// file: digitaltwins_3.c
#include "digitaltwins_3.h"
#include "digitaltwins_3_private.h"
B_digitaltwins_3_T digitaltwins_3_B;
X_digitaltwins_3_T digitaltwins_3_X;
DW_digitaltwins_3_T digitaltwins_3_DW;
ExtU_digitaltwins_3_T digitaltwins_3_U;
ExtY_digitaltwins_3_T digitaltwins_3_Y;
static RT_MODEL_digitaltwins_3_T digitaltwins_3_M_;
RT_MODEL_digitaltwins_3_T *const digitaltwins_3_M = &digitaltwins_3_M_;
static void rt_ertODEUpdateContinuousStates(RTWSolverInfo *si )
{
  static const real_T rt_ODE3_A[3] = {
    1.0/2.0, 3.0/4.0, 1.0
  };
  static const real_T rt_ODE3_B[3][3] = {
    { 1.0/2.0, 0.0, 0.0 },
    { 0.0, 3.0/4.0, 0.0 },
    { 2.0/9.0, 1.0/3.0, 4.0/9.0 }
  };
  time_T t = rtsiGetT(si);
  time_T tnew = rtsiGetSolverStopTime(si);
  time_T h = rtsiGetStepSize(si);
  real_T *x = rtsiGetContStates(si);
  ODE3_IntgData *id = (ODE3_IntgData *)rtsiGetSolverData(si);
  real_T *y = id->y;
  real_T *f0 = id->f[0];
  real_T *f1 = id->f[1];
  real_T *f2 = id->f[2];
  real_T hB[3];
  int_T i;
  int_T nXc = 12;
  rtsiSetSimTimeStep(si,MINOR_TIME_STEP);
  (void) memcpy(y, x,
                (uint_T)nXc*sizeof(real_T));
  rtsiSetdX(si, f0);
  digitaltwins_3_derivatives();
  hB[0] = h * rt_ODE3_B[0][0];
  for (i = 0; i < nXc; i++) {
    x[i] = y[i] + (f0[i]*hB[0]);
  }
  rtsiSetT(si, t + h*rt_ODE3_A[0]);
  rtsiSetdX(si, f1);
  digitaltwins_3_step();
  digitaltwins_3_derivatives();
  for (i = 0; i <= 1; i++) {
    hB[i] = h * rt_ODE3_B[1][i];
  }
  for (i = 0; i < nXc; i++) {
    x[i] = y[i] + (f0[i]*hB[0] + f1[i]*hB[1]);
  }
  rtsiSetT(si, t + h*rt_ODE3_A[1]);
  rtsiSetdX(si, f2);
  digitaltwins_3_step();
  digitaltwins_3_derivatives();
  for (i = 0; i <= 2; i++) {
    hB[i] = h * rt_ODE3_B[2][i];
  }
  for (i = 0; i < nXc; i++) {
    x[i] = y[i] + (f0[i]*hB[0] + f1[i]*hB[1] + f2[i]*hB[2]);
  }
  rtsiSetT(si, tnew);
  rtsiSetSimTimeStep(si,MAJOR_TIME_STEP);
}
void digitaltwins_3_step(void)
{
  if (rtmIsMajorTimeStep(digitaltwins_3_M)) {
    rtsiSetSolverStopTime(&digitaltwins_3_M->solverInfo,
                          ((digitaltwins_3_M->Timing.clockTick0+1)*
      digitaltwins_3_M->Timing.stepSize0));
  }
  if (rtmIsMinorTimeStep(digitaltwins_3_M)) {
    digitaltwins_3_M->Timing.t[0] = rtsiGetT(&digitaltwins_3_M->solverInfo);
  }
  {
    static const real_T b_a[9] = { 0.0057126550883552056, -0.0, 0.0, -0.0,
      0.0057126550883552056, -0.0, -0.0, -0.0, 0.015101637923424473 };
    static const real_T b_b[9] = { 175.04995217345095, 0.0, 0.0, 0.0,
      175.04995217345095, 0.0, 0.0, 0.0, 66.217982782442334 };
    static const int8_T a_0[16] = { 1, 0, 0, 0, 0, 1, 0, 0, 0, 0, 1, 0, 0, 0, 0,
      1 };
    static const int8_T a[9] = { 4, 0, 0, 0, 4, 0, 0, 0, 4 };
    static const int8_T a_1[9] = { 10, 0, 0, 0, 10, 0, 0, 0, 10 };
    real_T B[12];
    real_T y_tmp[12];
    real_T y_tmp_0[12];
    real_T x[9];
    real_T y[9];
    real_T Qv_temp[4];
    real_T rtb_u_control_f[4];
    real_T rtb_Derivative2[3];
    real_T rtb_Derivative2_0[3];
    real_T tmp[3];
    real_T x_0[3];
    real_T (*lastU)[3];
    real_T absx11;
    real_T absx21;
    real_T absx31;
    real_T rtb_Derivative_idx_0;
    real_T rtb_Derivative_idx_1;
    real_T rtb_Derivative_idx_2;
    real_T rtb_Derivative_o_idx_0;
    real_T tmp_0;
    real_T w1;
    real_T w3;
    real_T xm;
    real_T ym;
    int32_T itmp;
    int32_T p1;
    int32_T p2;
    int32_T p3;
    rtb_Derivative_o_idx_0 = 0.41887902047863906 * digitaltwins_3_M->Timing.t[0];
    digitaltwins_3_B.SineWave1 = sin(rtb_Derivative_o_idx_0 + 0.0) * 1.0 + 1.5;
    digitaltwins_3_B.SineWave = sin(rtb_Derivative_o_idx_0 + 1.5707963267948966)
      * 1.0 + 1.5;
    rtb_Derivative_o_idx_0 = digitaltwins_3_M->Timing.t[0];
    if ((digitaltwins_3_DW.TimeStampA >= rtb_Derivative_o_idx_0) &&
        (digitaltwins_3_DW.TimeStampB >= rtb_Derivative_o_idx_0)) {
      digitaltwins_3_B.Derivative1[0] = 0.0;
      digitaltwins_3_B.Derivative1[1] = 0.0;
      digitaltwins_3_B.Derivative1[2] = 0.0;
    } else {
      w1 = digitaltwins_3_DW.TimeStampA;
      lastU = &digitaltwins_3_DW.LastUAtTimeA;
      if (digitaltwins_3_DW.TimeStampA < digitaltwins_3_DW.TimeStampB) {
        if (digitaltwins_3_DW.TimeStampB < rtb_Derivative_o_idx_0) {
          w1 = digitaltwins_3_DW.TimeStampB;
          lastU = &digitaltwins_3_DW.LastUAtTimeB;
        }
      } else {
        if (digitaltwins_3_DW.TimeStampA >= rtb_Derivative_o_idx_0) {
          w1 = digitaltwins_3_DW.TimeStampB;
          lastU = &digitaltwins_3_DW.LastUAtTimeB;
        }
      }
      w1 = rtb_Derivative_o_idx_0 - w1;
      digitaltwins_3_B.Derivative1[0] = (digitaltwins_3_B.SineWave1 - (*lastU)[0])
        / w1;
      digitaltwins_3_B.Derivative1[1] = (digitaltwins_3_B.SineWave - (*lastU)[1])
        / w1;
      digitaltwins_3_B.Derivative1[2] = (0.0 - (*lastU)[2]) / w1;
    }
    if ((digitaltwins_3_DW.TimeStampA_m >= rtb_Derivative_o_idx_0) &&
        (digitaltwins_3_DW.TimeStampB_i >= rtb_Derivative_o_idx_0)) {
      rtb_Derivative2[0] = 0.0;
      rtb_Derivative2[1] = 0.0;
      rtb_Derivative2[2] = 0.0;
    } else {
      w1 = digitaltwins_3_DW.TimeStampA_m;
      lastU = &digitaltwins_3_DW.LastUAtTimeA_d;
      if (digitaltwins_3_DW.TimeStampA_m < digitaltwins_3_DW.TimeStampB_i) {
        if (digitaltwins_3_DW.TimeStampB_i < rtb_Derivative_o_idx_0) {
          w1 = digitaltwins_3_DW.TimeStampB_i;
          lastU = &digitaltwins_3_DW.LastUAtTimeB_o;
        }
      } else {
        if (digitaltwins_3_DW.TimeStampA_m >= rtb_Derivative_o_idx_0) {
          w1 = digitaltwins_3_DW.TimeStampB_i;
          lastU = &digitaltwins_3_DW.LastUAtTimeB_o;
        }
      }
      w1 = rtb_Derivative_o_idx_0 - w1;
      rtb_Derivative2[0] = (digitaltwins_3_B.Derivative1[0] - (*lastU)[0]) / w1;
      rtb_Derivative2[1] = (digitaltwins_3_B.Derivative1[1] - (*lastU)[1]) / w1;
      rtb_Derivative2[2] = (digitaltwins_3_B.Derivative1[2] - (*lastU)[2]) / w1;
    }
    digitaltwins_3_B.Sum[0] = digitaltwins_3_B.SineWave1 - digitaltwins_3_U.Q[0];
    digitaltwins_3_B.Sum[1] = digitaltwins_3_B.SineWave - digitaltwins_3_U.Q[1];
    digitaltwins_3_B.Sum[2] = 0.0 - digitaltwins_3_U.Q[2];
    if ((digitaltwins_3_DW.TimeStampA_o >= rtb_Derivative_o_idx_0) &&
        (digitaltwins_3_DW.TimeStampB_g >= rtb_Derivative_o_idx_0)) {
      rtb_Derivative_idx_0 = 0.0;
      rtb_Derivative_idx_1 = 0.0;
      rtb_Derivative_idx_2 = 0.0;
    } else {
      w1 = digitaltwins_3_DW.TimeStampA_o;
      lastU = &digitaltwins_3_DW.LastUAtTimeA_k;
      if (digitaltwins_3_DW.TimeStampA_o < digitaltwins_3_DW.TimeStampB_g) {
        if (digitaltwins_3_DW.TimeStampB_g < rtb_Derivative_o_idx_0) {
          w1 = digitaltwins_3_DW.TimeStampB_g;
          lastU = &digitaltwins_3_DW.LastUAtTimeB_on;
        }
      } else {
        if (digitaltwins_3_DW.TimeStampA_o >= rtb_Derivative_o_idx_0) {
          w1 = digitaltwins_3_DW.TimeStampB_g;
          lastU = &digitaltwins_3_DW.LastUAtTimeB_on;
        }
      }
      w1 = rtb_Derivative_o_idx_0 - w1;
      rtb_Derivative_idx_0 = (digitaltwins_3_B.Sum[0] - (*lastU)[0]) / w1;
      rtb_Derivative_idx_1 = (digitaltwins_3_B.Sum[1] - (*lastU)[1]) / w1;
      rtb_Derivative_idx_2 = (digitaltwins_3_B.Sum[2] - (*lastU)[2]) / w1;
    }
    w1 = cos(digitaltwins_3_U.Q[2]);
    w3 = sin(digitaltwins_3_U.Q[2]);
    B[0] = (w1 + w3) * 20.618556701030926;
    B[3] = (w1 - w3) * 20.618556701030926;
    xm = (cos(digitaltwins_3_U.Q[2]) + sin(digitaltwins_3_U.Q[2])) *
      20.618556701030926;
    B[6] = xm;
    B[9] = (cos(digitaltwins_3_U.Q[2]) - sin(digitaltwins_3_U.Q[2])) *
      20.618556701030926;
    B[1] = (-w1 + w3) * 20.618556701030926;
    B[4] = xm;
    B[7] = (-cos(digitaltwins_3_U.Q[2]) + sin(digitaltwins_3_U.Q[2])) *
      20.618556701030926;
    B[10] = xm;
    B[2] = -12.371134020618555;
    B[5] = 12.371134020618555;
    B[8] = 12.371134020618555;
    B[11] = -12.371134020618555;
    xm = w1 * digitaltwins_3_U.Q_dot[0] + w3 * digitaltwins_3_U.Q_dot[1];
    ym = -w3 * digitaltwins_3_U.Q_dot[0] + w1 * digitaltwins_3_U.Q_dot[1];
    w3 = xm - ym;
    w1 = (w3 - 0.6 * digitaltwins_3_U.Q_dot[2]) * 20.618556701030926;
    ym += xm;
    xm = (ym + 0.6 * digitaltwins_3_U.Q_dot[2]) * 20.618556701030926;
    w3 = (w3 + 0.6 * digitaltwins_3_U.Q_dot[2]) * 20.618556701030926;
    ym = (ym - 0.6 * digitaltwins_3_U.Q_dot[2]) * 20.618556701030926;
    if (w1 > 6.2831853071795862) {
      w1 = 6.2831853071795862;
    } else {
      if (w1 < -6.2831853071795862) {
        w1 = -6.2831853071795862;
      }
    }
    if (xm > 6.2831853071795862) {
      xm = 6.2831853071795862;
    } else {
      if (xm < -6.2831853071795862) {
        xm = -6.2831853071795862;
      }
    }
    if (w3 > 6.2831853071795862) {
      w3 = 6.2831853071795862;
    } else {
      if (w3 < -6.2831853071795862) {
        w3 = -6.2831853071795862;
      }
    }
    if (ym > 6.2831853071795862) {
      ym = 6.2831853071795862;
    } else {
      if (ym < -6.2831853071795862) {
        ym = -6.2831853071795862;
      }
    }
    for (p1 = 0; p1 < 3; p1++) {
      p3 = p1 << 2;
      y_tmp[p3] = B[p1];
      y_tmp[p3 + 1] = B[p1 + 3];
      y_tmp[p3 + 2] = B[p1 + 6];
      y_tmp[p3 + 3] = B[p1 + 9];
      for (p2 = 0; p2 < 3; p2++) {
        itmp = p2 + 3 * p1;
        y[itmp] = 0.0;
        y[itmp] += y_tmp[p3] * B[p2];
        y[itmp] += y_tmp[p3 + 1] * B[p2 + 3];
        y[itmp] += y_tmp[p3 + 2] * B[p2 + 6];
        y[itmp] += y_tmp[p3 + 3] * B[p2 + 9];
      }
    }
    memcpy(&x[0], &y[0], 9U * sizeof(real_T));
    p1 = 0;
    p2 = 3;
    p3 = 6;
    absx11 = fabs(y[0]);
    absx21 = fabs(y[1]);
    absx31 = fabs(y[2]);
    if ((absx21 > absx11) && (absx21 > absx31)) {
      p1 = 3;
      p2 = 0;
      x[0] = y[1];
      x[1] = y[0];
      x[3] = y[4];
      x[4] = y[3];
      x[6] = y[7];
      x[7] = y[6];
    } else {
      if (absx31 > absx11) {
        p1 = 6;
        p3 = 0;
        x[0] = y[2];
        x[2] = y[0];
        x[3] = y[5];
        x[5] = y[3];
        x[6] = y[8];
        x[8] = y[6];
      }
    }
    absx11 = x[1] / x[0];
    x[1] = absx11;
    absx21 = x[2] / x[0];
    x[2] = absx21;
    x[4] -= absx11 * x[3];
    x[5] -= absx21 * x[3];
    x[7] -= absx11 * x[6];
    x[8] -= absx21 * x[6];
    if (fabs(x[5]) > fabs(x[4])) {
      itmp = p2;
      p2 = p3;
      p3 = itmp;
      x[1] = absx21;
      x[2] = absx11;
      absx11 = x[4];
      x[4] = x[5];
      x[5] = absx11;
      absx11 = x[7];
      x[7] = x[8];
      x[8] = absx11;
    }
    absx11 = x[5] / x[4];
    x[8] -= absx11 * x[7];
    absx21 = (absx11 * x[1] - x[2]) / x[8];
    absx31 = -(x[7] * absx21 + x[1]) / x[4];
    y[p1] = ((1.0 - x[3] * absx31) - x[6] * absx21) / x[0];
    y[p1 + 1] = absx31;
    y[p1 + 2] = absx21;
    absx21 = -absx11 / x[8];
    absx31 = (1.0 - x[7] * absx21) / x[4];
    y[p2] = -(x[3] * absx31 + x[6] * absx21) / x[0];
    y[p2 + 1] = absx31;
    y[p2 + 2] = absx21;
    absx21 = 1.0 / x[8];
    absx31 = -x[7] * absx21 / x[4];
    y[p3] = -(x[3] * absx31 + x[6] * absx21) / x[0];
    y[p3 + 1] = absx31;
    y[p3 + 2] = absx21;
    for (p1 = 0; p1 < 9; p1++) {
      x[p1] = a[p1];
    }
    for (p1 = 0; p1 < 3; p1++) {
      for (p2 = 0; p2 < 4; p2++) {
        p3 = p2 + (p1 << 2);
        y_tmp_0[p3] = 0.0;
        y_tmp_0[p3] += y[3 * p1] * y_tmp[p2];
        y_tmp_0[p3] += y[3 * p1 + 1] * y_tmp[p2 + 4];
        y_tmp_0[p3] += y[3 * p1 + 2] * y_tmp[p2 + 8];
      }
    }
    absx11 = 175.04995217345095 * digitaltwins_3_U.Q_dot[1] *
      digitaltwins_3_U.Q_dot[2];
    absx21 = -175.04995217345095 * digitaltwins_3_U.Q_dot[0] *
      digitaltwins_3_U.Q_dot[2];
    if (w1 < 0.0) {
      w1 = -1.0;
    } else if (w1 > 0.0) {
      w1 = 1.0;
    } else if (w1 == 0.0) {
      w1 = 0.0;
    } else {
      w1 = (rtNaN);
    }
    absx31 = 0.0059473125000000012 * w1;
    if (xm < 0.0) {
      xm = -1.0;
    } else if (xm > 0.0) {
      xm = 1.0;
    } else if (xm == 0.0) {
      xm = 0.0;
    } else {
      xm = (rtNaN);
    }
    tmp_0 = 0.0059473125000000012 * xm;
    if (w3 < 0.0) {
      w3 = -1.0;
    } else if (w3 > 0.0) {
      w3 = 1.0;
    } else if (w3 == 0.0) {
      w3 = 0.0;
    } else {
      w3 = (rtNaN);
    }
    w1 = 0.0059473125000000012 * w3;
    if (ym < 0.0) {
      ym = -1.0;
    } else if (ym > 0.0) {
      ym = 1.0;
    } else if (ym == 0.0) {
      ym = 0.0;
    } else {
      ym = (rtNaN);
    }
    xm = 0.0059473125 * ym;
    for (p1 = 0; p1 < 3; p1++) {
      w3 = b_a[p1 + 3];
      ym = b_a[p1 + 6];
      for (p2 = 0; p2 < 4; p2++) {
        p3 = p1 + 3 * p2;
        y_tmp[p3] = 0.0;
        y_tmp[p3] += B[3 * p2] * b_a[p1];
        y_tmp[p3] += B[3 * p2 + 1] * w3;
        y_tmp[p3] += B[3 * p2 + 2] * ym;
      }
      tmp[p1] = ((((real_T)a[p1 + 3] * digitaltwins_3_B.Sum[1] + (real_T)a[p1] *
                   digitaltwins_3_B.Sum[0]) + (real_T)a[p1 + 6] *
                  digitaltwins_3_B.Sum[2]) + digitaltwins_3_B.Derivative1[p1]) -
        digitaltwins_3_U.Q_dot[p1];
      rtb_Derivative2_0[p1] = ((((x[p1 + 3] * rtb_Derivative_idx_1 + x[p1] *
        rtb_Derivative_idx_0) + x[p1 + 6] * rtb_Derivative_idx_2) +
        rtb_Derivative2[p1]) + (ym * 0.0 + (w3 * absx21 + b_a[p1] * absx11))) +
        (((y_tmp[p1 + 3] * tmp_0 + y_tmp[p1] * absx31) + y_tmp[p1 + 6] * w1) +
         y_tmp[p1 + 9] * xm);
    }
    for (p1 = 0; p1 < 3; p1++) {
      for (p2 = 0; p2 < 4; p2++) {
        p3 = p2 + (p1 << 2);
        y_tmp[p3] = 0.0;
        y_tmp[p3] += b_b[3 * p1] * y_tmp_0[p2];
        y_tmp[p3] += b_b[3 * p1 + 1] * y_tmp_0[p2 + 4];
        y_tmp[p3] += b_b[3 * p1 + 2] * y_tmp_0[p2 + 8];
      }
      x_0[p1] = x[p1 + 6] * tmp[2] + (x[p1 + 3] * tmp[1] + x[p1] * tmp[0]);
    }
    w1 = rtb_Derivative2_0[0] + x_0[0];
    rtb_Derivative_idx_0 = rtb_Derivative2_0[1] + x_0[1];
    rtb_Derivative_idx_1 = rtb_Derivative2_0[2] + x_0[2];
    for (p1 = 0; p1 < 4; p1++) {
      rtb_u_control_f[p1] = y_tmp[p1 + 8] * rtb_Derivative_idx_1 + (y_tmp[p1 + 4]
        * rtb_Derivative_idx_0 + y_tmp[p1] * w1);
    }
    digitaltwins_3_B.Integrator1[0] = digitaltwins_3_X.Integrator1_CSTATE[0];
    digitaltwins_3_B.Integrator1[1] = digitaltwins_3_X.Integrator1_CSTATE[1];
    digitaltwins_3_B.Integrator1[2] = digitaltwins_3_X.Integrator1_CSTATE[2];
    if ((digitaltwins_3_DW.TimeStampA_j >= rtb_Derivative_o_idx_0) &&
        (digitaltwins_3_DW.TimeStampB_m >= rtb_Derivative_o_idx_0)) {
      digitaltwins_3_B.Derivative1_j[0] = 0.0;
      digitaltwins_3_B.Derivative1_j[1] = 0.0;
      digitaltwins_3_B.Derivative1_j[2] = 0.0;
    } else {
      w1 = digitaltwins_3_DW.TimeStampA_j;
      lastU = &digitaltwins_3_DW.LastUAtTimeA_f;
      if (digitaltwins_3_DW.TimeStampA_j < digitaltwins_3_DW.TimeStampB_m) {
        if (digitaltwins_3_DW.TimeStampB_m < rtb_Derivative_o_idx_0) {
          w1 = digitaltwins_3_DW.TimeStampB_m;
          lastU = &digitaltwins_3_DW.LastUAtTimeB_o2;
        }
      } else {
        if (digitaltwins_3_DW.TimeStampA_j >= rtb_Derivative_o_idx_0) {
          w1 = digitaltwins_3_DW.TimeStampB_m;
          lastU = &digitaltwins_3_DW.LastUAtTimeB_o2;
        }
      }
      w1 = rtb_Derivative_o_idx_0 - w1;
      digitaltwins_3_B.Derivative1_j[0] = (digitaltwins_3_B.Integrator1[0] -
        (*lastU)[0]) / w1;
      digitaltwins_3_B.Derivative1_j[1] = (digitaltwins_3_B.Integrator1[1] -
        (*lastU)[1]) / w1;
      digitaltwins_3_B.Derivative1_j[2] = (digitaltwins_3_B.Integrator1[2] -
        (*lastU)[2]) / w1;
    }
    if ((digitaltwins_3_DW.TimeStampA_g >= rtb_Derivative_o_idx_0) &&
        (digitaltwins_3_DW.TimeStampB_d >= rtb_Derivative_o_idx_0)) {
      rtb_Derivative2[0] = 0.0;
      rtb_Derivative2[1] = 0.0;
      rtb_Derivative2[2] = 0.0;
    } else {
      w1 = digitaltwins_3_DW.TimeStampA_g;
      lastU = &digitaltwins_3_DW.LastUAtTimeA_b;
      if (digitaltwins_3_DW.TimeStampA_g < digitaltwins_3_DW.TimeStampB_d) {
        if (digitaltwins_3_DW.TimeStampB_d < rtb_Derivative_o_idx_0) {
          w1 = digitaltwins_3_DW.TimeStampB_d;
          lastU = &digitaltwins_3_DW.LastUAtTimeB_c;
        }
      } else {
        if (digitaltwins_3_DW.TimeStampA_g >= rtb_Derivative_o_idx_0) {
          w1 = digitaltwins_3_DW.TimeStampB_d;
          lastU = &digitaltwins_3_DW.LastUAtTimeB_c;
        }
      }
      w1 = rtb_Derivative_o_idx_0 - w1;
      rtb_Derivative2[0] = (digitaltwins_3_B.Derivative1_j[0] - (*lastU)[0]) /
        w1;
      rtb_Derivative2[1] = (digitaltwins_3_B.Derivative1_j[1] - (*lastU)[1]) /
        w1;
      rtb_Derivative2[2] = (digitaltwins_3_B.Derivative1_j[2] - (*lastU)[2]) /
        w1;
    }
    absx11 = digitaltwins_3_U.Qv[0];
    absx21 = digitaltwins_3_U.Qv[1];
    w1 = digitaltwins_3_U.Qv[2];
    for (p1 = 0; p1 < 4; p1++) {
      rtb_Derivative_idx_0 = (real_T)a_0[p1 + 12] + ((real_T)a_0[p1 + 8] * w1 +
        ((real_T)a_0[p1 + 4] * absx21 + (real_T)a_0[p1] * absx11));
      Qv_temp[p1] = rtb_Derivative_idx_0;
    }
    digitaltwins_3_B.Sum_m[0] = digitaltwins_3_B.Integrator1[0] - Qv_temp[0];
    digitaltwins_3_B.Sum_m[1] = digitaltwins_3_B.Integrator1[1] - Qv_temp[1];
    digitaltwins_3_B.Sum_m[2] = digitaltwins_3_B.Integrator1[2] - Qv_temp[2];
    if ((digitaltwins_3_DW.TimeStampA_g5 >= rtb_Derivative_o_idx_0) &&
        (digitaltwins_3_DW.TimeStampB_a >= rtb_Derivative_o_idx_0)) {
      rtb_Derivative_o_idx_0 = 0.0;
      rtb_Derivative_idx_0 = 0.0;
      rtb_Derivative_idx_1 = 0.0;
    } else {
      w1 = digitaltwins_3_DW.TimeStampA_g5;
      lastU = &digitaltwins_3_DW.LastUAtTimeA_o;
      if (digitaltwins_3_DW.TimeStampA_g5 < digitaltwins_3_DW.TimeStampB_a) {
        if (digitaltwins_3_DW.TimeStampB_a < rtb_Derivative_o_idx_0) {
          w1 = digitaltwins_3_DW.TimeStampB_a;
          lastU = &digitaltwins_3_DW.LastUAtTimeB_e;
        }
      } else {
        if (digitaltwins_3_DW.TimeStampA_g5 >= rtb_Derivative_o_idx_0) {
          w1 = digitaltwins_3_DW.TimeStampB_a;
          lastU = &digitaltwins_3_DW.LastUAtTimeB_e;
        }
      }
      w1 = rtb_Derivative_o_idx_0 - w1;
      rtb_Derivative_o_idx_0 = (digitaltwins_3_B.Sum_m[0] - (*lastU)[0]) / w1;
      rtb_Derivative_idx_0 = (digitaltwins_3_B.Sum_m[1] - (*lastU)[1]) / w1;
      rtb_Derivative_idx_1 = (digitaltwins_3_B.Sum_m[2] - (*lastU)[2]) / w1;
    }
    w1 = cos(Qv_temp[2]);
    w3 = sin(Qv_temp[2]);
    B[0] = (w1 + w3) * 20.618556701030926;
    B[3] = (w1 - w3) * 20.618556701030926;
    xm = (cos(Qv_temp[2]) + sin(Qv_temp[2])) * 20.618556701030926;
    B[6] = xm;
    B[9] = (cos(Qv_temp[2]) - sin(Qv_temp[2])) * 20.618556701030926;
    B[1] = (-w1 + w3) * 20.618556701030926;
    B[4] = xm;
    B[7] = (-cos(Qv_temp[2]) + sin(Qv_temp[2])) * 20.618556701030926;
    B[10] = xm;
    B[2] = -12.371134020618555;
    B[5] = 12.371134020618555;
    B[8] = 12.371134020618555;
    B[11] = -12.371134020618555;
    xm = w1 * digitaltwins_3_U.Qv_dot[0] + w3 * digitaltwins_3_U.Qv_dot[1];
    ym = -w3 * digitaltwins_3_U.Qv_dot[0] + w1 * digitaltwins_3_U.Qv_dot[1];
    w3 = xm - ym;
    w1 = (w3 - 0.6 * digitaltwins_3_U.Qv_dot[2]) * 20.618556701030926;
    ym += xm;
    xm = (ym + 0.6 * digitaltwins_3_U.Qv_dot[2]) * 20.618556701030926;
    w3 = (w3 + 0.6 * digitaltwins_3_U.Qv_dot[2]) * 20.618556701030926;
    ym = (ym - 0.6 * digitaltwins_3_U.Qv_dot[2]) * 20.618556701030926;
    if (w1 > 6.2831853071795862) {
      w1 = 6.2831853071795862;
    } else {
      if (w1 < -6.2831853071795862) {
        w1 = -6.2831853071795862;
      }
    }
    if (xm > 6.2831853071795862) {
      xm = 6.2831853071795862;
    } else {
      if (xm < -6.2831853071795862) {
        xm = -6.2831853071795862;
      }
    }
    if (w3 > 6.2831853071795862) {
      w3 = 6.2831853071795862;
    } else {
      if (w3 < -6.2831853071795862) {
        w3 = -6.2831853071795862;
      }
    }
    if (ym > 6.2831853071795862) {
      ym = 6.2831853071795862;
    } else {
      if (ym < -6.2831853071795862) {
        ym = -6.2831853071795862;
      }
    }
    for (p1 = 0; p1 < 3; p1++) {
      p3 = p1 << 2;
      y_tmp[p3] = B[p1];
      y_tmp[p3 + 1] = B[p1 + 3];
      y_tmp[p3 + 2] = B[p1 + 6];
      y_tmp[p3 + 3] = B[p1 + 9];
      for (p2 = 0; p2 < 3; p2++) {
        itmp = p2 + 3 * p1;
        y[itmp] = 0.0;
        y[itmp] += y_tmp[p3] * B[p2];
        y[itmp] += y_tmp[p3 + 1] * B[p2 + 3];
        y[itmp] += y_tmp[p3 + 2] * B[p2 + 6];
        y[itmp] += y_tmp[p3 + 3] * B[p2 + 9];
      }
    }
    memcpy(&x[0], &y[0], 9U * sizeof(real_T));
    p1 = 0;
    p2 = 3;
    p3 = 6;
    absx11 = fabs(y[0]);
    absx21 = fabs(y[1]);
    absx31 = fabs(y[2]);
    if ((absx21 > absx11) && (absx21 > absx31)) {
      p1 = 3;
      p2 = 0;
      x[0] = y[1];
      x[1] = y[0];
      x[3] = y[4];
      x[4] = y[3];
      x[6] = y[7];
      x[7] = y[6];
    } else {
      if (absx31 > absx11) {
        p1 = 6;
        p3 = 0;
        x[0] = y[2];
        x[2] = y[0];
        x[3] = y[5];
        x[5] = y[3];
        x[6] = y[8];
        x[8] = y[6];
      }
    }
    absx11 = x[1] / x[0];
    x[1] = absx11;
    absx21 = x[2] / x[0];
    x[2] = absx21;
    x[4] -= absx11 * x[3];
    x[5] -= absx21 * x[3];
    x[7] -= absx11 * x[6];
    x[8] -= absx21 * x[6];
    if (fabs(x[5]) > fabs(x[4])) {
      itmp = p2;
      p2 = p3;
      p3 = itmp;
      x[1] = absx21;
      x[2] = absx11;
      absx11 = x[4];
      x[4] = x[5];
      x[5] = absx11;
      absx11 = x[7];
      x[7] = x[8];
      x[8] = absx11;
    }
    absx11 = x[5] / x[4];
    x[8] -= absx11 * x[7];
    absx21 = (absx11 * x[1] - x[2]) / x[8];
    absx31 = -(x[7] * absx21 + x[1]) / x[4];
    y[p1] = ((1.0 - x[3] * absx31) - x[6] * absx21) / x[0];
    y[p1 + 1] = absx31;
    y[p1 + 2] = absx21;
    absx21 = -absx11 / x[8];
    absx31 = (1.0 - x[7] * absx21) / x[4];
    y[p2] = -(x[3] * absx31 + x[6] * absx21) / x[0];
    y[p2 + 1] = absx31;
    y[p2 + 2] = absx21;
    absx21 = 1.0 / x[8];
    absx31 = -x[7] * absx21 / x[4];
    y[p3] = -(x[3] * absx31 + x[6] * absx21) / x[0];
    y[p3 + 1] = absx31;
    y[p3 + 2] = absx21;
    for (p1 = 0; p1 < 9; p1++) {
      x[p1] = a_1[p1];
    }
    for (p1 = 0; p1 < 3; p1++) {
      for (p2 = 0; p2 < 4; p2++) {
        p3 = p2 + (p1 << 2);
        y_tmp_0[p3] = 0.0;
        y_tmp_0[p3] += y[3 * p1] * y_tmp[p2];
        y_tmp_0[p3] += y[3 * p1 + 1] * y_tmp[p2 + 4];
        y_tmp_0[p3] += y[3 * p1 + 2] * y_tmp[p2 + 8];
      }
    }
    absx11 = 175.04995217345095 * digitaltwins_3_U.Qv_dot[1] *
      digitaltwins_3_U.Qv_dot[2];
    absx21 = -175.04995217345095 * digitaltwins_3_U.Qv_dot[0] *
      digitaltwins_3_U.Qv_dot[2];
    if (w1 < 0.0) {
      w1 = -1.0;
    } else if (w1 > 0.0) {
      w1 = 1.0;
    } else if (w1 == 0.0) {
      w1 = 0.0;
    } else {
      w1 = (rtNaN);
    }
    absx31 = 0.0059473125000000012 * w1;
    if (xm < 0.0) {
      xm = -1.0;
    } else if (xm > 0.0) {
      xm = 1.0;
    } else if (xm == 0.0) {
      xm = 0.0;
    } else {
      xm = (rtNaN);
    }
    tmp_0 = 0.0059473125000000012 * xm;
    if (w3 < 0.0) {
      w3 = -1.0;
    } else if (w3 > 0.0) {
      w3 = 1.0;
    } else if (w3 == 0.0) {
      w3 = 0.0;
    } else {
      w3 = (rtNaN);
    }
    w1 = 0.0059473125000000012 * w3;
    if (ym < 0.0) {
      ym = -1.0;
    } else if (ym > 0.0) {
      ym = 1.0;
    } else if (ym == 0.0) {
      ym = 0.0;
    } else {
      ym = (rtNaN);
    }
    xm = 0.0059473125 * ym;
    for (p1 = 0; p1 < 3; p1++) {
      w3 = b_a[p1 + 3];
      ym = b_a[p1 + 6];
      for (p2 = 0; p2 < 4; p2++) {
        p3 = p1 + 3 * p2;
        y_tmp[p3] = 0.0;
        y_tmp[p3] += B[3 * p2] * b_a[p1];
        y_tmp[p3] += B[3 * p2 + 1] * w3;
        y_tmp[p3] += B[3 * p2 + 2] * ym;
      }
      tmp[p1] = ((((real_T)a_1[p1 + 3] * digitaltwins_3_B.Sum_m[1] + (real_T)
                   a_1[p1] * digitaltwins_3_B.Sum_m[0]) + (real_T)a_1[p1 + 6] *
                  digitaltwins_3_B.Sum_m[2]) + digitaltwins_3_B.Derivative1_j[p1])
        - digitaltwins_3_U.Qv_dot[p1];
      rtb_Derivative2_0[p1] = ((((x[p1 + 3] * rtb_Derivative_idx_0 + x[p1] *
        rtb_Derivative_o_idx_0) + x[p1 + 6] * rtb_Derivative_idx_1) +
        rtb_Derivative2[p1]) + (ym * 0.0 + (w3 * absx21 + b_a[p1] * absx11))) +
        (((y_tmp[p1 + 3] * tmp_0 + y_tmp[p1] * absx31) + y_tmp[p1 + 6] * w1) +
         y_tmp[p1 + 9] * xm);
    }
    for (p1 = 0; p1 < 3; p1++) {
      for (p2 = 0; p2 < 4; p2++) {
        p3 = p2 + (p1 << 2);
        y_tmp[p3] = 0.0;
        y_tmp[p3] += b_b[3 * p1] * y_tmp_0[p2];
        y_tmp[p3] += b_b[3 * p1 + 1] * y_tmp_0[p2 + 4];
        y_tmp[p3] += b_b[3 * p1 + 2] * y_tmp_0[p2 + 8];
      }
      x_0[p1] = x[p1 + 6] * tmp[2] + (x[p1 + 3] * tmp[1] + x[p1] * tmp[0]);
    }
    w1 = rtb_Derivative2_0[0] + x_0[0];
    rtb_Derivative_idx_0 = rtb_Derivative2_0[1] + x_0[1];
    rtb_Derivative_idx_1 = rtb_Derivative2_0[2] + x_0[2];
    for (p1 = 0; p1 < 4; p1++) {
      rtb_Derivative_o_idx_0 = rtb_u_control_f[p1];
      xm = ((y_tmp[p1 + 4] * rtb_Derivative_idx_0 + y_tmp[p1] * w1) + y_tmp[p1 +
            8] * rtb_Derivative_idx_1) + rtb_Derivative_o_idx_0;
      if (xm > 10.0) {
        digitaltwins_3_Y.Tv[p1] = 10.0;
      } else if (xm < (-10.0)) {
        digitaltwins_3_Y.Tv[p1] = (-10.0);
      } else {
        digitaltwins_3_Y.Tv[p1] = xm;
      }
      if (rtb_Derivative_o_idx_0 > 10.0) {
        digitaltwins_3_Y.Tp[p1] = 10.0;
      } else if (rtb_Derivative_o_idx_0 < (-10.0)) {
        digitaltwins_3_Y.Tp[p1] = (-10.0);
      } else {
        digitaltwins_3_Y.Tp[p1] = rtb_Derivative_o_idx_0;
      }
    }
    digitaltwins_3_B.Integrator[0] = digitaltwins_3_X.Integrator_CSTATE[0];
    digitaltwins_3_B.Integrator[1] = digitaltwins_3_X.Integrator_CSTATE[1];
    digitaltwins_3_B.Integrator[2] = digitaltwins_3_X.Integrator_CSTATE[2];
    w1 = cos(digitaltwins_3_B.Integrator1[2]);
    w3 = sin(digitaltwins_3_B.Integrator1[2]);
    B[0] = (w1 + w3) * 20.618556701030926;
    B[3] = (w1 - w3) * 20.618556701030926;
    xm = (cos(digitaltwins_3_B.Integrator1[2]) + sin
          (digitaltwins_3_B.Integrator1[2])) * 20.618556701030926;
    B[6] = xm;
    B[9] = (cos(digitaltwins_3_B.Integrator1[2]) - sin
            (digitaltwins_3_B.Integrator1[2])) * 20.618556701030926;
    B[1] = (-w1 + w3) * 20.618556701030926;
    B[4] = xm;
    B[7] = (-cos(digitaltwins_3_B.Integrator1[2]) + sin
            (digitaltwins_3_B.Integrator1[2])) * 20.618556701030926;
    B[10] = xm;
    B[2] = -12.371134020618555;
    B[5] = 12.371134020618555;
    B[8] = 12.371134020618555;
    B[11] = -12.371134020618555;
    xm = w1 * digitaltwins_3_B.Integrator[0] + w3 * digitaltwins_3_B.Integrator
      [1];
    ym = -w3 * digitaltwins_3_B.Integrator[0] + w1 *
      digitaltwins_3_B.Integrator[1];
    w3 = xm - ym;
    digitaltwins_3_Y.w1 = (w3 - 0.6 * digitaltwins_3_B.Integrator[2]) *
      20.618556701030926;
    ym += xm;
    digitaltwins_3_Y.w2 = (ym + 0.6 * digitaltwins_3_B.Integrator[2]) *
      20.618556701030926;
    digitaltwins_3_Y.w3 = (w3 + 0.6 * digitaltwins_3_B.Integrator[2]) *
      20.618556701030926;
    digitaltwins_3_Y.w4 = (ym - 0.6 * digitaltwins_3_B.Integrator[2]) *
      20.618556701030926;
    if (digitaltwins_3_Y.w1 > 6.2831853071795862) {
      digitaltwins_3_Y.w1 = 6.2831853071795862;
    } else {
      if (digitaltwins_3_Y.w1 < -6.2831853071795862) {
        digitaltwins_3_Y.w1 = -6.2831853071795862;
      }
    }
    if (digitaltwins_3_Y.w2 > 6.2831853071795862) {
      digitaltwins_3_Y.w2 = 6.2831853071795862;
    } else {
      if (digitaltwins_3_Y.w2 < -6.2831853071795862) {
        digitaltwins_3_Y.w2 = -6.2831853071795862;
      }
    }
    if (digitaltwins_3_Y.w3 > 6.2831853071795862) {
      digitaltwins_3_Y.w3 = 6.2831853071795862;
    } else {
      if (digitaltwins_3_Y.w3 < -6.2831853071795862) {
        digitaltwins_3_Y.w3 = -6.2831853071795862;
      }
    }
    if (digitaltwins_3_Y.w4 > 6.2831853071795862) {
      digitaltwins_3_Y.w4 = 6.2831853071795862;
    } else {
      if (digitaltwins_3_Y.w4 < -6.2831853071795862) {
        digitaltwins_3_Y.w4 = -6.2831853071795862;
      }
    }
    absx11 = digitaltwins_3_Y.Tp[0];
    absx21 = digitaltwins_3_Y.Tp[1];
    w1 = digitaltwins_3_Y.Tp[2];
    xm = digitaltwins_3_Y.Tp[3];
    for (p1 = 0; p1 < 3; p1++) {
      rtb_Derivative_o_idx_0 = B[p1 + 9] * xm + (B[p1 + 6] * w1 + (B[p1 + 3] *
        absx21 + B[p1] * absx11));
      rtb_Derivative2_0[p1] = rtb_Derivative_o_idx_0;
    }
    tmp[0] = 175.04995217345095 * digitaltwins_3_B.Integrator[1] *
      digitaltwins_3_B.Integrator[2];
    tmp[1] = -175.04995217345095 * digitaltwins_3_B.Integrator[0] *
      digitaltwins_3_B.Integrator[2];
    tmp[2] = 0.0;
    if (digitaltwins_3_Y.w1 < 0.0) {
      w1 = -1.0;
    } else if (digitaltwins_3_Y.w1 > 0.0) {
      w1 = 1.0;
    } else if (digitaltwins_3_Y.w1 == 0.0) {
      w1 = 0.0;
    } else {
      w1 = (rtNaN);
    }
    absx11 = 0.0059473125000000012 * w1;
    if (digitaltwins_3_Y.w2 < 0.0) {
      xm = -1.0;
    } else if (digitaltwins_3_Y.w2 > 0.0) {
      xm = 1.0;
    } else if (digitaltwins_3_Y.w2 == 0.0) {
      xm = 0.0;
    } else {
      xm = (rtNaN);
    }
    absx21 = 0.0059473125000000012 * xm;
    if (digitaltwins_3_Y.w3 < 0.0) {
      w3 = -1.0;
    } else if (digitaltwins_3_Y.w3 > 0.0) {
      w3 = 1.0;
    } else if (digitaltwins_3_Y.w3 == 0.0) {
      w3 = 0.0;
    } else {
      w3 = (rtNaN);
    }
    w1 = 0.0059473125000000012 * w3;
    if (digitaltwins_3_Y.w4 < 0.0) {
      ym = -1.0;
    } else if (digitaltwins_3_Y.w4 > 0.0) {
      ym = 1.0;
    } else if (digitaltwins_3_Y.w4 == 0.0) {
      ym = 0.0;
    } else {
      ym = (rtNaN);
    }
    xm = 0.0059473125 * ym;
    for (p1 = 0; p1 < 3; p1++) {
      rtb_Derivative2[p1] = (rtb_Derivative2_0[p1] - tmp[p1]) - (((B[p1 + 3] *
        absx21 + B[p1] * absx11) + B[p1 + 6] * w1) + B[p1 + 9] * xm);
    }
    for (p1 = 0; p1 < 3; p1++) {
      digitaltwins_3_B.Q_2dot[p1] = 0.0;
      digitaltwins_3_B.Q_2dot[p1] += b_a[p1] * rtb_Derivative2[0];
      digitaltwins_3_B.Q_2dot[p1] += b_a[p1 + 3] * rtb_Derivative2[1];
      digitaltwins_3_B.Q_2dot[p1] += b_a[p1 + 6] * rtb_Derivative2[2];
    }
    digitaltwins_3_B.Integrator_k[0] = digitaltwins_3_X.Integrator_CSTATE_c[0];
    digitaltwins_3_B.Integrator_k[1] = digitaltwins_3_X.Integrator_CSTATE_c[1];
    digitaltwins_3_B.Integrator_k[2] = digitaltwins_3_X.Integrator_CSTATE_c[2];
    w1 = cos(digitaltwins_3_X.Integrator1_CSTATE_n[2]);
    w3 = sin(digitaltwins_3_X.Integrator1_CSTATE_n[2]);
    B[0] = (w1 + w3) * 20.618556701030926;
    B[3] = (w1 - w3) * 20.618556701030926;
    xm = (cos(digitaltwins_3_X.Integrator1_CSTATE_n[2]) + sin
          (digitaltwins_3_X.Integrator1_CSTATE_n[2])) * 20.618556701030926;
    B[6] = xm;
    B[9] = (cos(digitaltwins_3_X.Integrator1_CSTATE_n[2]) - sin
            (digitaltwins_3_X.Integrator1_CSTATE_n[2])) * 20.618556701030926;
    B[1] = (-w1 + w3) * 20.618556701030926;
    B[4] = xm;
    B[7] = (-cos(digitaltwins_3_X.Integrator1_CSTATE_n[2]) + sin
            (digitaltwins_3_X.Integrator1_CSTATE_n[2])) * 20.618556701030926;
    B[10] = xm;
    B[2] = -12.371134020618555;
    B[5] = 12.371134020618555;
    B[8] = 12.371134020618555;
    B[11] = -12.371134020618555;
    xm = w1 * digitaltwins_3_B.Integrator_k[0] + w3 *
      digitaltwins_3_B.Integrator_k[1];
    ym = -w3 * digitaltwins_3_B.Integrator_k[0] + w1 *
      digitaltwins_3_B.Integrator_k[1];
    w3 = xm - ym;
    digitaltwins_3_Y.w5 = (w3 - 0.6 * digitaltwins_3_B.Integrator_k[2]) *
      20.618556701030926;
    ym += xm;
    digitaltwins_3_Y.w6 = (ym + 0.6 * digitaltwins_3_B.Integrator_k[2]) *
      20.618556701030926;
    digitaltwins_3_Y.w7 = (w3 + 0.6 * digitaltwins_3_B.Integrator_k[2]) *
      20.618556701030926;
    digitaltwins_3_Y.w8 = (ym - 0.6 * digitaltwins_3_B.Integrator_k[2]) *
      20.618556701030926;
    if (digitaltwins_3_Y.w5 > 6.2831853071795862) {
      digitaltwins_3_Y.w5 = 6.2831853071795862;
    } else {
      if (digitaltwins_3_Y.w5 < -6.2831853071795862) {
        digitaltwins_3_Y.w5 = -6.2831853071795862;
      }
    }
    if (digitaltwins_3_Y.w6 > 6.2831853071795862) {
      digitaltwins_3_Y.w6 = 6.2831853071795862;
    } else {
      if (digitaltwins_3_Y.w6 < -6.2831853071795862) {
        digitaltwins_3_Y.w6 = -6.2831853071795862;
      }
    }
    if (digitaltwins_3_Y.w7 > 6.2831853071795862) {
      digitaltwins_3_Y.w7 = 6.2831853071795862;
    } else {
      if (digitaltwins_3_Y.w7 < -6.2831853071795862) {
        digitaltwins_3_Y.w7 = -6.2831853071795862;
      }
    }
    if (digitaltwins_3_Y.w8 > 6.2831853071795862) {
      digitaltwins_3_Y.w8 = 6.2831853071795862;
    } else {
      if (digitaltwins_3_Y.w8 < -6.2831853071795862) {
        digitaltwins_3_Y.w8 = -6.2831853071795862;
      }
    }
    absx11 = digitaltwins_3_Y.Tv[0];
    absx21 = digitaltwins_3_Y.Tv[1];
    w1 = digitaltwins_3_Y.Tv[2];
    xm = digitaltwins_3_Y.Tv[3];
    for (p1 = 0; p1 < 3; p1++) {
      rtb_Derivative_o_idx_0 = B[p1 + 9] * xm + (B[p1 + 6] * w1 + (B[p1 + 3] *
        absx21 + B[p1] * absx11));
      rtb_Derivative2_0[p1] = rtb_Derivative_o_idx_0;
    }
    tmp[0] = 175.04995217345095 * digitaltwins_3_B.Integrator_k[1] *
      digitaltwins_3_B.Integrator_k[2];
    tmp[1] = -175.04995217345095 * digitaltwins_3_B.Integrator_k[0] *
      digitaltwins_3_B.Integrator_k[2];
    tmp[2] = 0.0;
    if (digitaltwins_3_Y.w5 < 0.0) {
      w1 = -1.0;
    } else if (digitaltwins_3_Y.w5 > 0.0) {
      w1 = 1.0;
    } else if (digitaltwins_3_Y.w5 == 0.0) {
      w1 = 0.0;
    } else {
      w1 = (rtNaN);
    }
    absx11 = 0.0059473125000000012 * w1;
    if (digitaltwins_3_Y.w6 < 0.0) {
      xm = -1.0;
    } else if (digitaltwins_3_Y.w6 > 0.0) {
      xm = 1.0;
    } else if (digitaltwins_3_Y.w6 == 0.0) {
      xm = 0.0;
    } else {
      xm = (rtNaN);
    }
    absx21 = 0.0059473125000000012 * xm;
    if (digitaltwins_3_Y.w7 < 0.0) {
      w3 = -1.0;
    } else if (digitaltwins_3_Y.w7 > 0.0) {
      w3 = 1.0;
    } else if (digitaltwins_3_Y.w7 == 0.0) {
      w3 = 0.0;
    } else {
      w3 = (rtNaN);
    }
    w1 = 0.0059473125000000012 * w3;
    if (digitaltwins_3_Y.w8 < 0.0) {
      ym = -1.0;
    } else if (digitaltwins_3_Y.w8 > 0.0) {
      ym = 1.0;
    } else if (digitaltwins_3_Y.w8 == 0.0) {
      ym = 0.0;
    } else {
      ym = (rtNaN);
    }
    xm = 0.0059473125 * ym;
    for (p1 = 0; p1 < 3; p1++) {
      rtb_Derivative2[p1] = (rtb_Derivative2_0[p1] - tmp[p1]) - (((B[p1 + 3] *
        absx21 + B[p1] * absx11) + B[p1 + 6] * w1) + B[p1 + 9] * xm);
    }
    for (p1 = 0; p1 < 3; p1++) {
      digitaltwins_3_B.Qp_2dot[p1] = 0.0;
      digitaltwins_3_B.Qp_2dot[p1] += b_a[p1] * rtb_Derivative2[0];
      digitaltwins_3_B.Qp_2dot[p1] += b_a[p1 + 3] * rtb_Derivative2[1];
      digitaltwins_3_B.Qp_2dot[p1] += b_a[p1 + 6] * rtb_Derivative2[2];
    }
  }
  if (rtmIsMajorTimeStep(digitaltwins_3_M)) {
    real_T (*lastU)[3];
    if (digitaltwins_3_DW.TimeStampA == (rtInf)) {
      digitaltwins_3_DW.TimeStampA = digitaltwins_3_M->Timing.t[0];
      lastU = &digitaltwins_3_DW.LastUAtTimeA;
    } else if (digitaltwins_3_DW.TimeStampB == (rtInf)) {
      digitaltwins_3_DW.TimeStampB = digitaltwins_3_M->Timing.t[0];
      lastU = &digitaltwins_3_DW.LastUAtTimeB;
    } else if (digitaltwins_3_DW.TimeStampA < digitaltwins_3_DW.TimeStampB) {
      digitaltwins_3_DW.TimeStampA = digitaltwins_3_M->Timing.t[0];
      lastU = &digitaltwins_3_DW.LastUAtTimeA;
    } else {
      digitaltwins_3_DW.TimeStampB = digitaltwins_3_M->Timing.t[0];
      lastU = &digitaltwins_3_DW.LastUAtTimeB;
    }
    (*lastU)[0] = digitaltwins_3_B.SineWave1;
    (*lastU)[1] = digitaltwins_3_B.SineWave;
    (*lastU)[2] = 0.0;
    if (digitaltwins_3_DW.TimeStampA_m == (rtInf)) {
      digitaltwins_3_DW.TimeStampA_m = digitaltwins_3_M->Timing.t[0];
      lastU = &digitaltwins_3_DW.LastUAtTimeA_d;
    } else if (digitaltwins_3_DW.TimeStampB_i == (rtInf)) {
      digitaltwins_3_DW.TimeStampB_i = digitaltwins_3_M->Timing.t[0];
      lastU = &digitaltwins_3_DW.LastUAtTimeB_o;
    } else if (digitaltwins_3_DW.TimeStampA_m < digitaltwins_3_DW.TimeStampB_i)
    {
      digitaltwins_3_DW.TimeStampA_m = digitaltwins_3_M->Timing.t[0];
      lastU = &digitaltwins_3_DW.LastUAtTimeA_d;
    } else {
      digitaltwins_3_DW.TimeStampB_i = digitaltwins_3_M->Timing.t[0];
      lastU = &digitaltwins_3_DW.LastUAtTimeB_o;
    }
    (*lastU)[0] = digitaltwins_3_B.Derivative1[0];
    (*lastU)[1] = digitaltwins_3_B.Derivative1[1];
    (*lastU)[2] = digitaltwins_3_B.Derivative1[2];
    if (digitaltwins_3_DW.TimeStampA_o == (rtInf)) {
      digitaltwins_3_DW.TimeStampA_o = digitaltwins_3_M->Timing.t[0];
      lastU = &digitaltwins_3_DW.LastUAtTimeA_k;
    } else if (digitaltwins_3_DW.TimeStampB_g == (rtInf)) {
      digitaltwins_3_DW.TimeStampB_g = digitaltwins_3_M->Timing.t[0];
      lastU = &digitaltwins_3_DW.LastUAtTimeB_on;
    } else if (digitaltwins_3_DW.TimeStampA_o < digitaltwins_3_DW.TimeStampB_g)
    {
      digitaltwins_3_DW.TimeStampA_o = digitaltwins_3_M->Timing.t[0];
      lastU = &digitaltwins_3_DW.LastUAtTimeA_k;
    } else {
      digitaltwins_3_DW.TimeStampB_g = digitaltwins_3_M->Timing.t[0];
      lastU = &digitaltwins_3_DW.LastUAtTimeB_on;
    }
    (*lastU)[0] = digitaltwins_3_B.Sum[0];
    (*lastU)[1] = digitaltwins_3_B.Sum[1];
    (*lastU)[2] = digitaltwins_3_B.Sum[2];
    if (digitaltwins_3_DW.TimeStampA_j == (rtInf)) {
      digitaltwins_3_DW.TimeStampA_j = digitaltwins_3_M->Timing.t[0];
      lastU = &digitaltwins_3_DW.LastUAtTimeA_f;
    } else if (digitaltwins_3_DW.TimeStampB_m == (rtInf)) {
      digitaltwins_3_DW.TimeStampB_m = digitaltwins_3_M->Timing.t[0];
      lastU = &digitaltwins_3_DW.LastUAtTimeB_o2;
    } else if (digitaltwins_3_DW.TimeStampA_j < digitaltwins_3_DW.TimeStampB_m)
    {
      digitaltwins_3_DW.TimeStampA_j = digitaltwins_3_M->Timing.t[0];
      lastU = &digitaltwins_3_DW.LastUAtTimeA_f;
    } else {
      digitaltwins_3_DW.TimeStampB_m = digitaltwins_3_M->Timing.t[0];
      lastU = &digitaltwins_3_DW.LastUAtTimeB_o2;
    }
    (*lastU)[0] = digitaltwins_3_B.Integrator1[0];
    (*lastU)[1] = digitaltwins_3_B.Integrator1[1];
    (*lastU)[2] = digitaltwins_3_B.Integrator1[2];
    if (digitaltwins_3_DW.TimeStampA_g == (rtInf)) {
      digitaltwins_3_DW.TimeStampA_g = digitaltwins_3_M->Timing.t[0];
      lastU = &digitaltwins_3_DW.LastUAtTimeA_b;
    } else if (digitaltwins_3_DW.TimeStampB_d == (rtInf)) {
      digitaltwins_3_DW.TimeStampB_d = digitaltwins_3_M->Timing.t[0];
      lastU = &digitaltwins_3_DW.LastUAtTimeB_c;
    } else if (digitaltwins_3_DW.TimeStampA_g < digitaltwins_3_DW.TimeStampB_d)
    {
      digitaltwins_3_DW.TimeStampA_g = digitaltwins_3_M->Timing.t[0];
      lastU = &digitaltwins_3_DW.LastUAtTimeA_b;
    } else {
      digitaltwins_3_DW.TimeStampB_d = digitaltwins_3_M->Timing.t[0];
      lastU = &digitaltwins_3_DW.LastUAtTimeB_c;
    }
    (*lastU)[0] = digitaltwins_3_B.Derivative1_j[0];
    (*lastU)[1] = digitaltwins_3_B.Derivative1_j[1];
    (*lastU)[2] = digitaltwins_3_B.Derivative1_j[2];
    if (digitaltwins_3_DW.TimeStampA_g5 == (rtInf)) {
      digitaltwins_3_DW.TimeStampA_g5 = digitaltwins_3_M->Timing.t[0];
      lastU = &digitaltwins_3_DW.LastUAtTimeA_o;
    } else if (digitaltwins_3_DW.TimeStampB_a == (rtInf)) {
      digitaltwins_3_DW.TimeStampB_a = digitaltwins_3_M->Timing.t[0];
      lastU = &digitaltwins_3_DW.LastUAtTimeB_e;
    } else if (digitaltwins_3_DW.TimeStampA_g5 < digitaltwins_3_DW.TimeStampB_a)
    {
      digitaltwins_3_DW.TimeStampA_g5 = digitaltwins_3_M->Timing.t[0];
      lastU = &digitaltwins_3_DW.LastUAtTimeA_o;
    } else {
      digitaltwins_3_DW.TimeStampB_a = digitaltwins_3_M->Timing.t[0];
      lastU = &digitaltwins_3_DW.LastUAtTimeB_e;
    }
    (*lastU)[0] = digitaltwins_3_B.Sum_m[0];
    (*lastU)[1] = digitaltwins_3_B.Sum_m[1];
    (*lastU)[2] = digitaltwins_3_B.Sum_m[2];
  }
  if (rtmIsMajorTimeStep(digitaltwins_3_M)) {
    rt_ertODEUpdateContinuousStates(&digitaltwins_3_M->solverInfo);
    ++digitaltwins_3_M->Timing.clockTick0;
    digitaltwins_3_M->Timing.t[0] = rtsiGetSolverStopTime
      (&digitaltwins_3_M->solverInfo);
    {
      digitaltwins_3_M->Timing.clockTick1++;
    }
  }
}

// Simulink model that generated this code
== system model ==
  Inport#1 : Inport
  Q_dot : Inport
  Qv : Inport
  Qv_dot : Inport
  w1 : Outport  <- 1: MATLABFunction#1/2
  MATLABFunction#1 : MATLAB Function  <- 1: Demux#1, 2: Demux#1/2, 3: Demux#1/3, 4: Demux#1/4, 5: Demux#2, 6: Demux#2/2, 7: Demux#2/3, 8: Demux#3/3
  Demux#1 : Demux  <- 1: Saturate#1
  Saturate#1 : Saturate  UpperLimit=10  LowerLimit=-10  <- 1: MATLABFunction#2
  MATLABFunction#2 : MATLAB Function  <- 1: Derivative2, 2: Derivative, 3: MATLABFunction#3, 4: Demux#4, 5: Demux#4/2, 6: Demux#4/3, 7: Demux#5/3
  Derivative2 : Derivative  <- 1: Derivative1
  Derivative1 : Derivative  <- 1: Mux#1
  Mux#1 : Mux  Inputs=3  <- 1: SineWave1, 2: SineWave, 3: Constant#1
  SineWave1 : Sin  Bias=1.5  Frequency=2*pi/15
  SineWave : Sin  Bias=1.5  Frequency=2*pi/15  Phase=pi/2
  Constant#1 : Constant  Value=0
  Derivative : Derivative  <- 1: Sum
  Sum : Sum  Inputs=+-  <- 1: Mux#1, 2: Inport#1
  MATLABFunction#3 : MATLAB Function  <- 1: Derivative1, 2: Q_dot, 3: Sum
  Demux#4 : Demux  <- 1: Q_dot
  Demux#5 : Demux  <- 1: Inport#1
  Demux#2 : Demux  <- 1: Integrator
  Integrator : Integrator  <- 1: MATLABFunction#1
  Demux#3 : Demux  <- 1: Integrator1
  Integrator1 : Integrator  InitialCondition=[1.5 1.5 0]  <- 1: Integrator
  w2 : Outport  <- 1: MATLABFunction#1/3
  w3 : Outport  <- 1: MATLABFunction#1/4
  w4 : Outport  <- 1: MATLABFunction#1/5
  w5 : Outport  <- 1: MATLABFunction#4/2
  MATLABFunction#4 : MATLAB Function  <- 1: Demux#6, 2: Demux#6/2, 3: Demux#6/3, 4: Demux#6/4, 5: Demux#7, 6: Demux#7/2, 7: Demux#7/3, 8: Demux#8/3
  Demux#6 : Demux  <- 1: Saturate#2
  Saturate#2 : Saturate  UpperLimit=10  LowerLimit=-10  <- 1: Sum#1
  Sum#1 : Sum  Inputs=++  <- 1: MATLABFunction#5, 2: MATLABFunction#2
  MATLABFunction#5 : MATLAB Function  <- 1: Derivative#1, 2: Derivative#2, 3: MATLABFunction#6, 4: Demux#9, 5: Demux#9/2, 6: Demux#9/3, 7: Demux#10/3
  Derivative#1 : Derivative  <- 1: Derivative#3
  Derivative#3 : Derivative  <- 1: Integrator1
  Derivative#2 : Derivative  <- 1: Sum#2
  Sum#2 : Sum  Inputs=+-  <- 1: Integrator1, 2: MATLABFunction#7
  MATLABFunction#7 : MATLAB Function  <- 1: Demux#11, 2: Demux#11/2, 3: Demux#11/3
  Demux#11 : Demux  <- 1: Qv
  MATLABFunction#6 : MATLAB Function  <- 1: Derivative#3, 2: Qv_dot, 3: Sum#2
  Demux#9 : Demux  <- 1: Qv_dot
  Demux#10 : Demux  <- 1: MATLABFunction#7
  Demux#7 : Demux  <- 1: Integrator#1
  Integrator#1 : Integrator  <- 1: MATLABFunction#4
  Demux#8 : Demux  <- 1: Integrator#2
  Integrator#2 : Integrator  InitialCondition=[1.5 1.5 0]  <- 1: Integrator#1
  w6 : Outport  <- 1: MATLABFunction#4/3
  w7 : Outport  <- 1: MATLABFunction#4/4
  w8 : Outport  <- 1: MATLABFunction#4/5
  Tp : Outport  <- 1: Saturate#1
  Tv : Outport  <- 1: Saturate#2
== matlab function x2r ==
function e2  = fcn(Qr_dot,Qp_dot,e1)

k1 = [10 0 0;
      0 10 0;
      0 0 10];
 
%x2r_dot = (Qr_2dot+k1*e1_dot);
x2r = Qr_dot + k1*e1;
e2 = x2r - Qp_dot;

== matlab function MATLABFunction#1 ==
function [Q_2dot,w1,w2,w3,w4] = fcn(T1, T2, T3, T4,x_dot,y_dot,theta_dot,theta)
m=5;
I=5;
Ib=0.1;
l1= 0.3;
l2=0.3;
r=0.097/2;
g=9.81;
u=0.01;
N = m*g/4;
M=[(m+4*Ib/(r*r)) 0 0; 0 (m+4*Ib/(r*r)) 0; 0 0 (I+4*Ib*(l1+l2)*(l1+l2)/(r*r))];
C= [(m+4*Ib/(r*r))*y_dot*theta_dot;-(m+4*Ib/(r*r))*x_dot*theta_dot;0 ];
B=(1/r)*[(cos(theta)+sin(theta)) (cos(theta)-sin(theta)) (cos(theta)+sin(theta)) (cos(theta)-sin(theta));
         (-cos(theta)+sin(theta)) (cos(theta)+sin(theta)) (-cos(theta)+sin(theta)) (cos(theta)+sin(theta)); 
         (-(l1+l2)) (l1+l2) (l1+l2) (-(l1+l2)) ];
T=[T1;T2;T3;T4];
xm= cos(theta)*x_dot+sin(theta)*y_dot;
ym= -sin(theta)*x_dot+cos(theta)*y_dot;
w1 = (1/r)*(xm-ym-(l1+l2)*theta_dot);
w2 = (1/r)*(xm+ym+(l1+l2)*theta_dot);
w3 = (1/r)*(xm-ym+(l1+l2)*theta_dot);
w4 = (1/r)*(xm+ym-(l1+l2)*theta_dot);
w_max = 2*pi;
if w1 > w_max
    w1 = w_max;
elseif w1 < -w_max
    w1 = -w_max;
end
if w2 > w_max
    w2 = w_max;
elseif w2 < -w_max
    w2 = -w_max;
end
if w3 > w_max
    w3 = w_max;
elseif w3 < -w_max
    w3 = -w_max;
end
if w4 > w_max
    w4 = w_max;
elseif w4 < -w_max
    w4 = -w_max;
end
Xi=[u*r*N*sign(w1);u*r*N*sign(w2);u*r*N*sign(w3);u*N*r*sign(w4)];

Q_2dot=inv(M)*(B*T-C-B*Xi);

== matlab function MATLAB Function ==
function u_control = fcn(Qr_2dot,e1_dot,e2,x_dot,y_dot,theta_dot,theta)

m=5;
I=5;
Ib=0.1;
l1= 0.3;
l2=0.3;
r=0.097/2;
g=9.81;
u=0.01;
N = m*g/4;
M=[(m+4*Ib/(r*r)) 0 0; 0 (m+4*Ib/(r*r)) 0; 0 0 (I+4*Ib*(l1+l2)*(l1+l2)/(r*r))];
C= [(m+4*Ib/(r*r))*y_dot*theta_dot;-(m+4*Ib/(r*r))*x_dot*theta_dot;0 ];
B=(1/r)*[(cos(theta)+sin(theta)) (cos(theta)-sin(theta)) (cos(theta)+sin(theta)) (cos(theta)-sin(theta));
    (-cos(theta)+sin(theta)) (cos(theta)+sin(theta)) (-cos(theta)+sin(theta)) (cos(theta)+sin(theta)); 
    (-(l1+l2)) (l1+l2) (l1+l2) (-(l1+l2)) ];

xm= cos(theta)*x_dot+sin(theta)*y_dot;
ym= -sin(theta)*x_dot+cos(theta)*y_dot;
w1 = (1/r)*(xm-ym-(l1+l2)*theta_dot);
w2 = (1/r)*(xm+ym+(l1+l2)*theta_dot);
w3 = (1/r)*(xm-ym+(l1+l2)*theta_dot);
w4 = (1/r)*(xm+ym-(l1+l2)*theta_dot);
w_max = 2*pi;
if w1 > w_max
    w1 = w_max;
elseif w1 < -w_max
    w1 = -w_max;
end
if w2 > w_max
    w2 = w_max;
elseif w2 < -w_max
    w2 = -w_max;
end
if w3 > w_max
    w3 = w_max;
elseif w3 < -w_max
    w3 = -w_max;
end
if w4 > w_max
    w4 = w_max;
elseif w4 < -w_max
    w4 = -w_max;
end
Xi=[u*r*N*sign(w1);u*r*N*sign(w2);u*r*N*sign(w3);u*N*r*sign(w4)];

k1 = [4 0 0;
      0 4 0;
      0 0 4];
k2 = [4 0 0;
      0 4 0;
      0 0 4];
  
u_control = B'*inv(B*B')*M*((Qr_2dot+k1*e1_dot)+inv(M)*C+inv(M)*B*Xi+k2*e2);

== matlab function x2r ==
function e2  = fcn(Qr_dot,Q_dot,e1)

k1 = [4 0 0;
      0 4 0;
      0 0 4];
 
%x2r_dot = (Qr_2dot+k1*e1_dot);
x2r = Qr_dot + k1*e1;
e2 = x2r - Q_dot;

== matlab function MATLABFunction#7 ==
function Qv_ = fcn(xv, yv,thetav)

xp_t0 = 1.5;
yp_t0 = 1.5;
thetap_t0 = 0;
xv_t0 = 1.5;
yv_t0 = 1.5;
thetav_t0 = 0;
delta_theta = thetap_t0 - thetav_t0;
delta_x = xp_t0 - xv_t0*cos(delta_theta) - yv_t0*sin(delta_theta);
delta_y = yp_t0 - xv_t0*sin(delta_theta) - yv_t0*cos(delta_theta);

T_delta = [ 1 0 0 delta_x;
            0 1 0 delta_y;
            0 0 1 delta_theta;
            0 0 0 1];
R_delta = [ cos(delta_theta) -sin(delta_theta) 0 0;
            sin(delta_theta) cos(delta_theta) 0 0;
            0 0 1 0;
            0 0 0 1 ];   
H = T_delta*R_delta;
Qv_temp = H*[ xv; yv; thetav; 1];
Qv_ = [Qv_temp(1);Qv_temp(2);Qv_temp(3)];

== matlab function MATLABFunction#4 ==
function [Qp_2dot,w1,w2,w3,w4]  = fcn(T1, T2, T3, T4,xp_dot,yp_dot,thetap_dot,theta)
m=5;
I=5;
Ib=0.1;
l1= 0.3;
l2=0.3;
r=0.097/2;
g=9.81;
u=0.01;
N = m*g/4;
M=[(m+4*Ib/(r*r)) 0 0; 0 (m+4*Ib/(r*r)) 0; 0 0 (I+4*Ib*(l1+l2)*(l1+l2)/(r*r))];
C= [(m+4*Ib/(r*r))*yp_dot*thetap_dot;-(m+4*Ib/(r*r))*xp_dot*thetap_dot;0 ];
B=(1/r)*[(cos(theta)+sin(theta)) (cos(theta)-sin(theta)) (cos(theta)+sin(theta)) (cos(theta)-sin(theta));
         (-cos(theta)+sin(theta)) (cos(theta)+sin(theta)) (-cos(theta)+sin(theta)) (cos(theta)+sin(theta)); 
         (-(l1+l2)) (l1+l2) (l1+l2) (-(l1+l2)) ];
T=[T1;T2;T3;T4];
xm= cos(theta)*xp_dot+sin(theta)*yp_dot;
ym= -sin(theta)*xp_dot+cos(theta)*yp_dot;
w1 = (1/r)*(xm-ym-(l1+l2)*thetap_dot);
w2 = (1/r)*(xm+ym+(l1+l2)*thetap_dot);
w3 = (1/r)*(xm-ym+(l1+l2)*thetap_dot);
w4 = (1/r)*(xm+ym-(l1+l2)*thetap_dot);
w_max = 2*pi;
if w1 > w_max
    w1 = w_max;
elseif w1 < -w_max
    w1 = -w_max;
end
if w2 > w_max
    w2 = w_max;
elseif w2 < -w_max
    w2 = -w_max;
end
if w3 > w_max
    w3 = w_max;
elseif w3 < -w_max
    w3 = -w_max;
end
if w4 > w_max
    w4 = w_max;
elseif w4 < -w_max
    w4 = -w_max;
end
Xi=[u*r*N*sign(w1);u*r*N*sign(w2);u*r*N*sign(w3);u*N*r*sign(w4)];

Qp_2dot=inv(M)*(B*T-C-B*Xi);

== matlab function MATLAB Function ==
function u_control = fcn(Qr_2dot,e1_dot,e2,xp_dot,yp_dot,thetap_dot,theta)

m=5;
I=5;
Ib=0.1;
l1= 0.3;
l2=0.3;
r=0.097/2;
g=9.81;
u=0.01;
N = m*g/4;
M=[(m+4*Ib/(r*r)) 0 0; 0 (m+4*Ib/(r*r)) 0; 0 0 (I+4*Ib*(l1+l2)*(l1+l2)/(r*r))];
C= [(m+4*Ib/(r*r))*yp_dot*thetap_dot;-(m+4*Ib/(r*r))*xp_dot*thetap_dot;0 ];
B=(1/r)*[(cos(theta)+sin(theta)) (cos(theta)-sin(theta)) (cos(theta)+sin(theta)) (cos(theta)-sin(theta));
    (-cos(theta)+sin(theta)) (cos(theta)+sin(theta)) (-cos(theta)+sin(theta)) (cos(theta)+sin(theta)); 
    (-(l1+l2)) (l1+l2) (l1+l2) (-(l1+l2)) ];

xm= cos(theta)*xp_dot+sin(theta)*yp_dot;
ym= -sin(theta)*xp_dot+cos(theta)*yp_dot;
w1 = (1/r)*(xm-ym-(l1+l2)*thetap_dot);
w2 = (1/r)*(xm+ym+(l1+l2)*thetap_dot);
w3 = (1/r)*(xm-ym+(l1+l2)*thetap_dot);
w4 = (1/r)*(xm+ym-(l1+l2)*thetap_dot);
w_max = 2*pi;
if w1 > w_max
    w1 = w_max;
elseif w1 < -w_max
    w1 = -w_max;
end
if w2 > w_max
    w2 = w_max;
elseif w2 < -w_max
    w2 = -w_max;
end
if w3 > w_max
    w3 = w_max;
elseif w3 < -w_max
    w3 = -w_max;
end
if w4 > w_max
    w4 = w_max;
elseif w4 < -w_max
    w4 = -w_max;
end
Xi=[u*r*N*sign(w1);u*r*N*sign(w2);u*r*N*sign(w3);u*N*r*sign(w4)];

k1 = [10 0 0;
      0 10 0;
      0 0 10];
k2 = [10 0 0;
      0 10 0;
      0 0 10];
  
u_control = B'*inv(B*B')*M*((Qr_2dot+k1*e1_dot)+inv(M)*C+inv(M)*B*Xi+k2*e2);
